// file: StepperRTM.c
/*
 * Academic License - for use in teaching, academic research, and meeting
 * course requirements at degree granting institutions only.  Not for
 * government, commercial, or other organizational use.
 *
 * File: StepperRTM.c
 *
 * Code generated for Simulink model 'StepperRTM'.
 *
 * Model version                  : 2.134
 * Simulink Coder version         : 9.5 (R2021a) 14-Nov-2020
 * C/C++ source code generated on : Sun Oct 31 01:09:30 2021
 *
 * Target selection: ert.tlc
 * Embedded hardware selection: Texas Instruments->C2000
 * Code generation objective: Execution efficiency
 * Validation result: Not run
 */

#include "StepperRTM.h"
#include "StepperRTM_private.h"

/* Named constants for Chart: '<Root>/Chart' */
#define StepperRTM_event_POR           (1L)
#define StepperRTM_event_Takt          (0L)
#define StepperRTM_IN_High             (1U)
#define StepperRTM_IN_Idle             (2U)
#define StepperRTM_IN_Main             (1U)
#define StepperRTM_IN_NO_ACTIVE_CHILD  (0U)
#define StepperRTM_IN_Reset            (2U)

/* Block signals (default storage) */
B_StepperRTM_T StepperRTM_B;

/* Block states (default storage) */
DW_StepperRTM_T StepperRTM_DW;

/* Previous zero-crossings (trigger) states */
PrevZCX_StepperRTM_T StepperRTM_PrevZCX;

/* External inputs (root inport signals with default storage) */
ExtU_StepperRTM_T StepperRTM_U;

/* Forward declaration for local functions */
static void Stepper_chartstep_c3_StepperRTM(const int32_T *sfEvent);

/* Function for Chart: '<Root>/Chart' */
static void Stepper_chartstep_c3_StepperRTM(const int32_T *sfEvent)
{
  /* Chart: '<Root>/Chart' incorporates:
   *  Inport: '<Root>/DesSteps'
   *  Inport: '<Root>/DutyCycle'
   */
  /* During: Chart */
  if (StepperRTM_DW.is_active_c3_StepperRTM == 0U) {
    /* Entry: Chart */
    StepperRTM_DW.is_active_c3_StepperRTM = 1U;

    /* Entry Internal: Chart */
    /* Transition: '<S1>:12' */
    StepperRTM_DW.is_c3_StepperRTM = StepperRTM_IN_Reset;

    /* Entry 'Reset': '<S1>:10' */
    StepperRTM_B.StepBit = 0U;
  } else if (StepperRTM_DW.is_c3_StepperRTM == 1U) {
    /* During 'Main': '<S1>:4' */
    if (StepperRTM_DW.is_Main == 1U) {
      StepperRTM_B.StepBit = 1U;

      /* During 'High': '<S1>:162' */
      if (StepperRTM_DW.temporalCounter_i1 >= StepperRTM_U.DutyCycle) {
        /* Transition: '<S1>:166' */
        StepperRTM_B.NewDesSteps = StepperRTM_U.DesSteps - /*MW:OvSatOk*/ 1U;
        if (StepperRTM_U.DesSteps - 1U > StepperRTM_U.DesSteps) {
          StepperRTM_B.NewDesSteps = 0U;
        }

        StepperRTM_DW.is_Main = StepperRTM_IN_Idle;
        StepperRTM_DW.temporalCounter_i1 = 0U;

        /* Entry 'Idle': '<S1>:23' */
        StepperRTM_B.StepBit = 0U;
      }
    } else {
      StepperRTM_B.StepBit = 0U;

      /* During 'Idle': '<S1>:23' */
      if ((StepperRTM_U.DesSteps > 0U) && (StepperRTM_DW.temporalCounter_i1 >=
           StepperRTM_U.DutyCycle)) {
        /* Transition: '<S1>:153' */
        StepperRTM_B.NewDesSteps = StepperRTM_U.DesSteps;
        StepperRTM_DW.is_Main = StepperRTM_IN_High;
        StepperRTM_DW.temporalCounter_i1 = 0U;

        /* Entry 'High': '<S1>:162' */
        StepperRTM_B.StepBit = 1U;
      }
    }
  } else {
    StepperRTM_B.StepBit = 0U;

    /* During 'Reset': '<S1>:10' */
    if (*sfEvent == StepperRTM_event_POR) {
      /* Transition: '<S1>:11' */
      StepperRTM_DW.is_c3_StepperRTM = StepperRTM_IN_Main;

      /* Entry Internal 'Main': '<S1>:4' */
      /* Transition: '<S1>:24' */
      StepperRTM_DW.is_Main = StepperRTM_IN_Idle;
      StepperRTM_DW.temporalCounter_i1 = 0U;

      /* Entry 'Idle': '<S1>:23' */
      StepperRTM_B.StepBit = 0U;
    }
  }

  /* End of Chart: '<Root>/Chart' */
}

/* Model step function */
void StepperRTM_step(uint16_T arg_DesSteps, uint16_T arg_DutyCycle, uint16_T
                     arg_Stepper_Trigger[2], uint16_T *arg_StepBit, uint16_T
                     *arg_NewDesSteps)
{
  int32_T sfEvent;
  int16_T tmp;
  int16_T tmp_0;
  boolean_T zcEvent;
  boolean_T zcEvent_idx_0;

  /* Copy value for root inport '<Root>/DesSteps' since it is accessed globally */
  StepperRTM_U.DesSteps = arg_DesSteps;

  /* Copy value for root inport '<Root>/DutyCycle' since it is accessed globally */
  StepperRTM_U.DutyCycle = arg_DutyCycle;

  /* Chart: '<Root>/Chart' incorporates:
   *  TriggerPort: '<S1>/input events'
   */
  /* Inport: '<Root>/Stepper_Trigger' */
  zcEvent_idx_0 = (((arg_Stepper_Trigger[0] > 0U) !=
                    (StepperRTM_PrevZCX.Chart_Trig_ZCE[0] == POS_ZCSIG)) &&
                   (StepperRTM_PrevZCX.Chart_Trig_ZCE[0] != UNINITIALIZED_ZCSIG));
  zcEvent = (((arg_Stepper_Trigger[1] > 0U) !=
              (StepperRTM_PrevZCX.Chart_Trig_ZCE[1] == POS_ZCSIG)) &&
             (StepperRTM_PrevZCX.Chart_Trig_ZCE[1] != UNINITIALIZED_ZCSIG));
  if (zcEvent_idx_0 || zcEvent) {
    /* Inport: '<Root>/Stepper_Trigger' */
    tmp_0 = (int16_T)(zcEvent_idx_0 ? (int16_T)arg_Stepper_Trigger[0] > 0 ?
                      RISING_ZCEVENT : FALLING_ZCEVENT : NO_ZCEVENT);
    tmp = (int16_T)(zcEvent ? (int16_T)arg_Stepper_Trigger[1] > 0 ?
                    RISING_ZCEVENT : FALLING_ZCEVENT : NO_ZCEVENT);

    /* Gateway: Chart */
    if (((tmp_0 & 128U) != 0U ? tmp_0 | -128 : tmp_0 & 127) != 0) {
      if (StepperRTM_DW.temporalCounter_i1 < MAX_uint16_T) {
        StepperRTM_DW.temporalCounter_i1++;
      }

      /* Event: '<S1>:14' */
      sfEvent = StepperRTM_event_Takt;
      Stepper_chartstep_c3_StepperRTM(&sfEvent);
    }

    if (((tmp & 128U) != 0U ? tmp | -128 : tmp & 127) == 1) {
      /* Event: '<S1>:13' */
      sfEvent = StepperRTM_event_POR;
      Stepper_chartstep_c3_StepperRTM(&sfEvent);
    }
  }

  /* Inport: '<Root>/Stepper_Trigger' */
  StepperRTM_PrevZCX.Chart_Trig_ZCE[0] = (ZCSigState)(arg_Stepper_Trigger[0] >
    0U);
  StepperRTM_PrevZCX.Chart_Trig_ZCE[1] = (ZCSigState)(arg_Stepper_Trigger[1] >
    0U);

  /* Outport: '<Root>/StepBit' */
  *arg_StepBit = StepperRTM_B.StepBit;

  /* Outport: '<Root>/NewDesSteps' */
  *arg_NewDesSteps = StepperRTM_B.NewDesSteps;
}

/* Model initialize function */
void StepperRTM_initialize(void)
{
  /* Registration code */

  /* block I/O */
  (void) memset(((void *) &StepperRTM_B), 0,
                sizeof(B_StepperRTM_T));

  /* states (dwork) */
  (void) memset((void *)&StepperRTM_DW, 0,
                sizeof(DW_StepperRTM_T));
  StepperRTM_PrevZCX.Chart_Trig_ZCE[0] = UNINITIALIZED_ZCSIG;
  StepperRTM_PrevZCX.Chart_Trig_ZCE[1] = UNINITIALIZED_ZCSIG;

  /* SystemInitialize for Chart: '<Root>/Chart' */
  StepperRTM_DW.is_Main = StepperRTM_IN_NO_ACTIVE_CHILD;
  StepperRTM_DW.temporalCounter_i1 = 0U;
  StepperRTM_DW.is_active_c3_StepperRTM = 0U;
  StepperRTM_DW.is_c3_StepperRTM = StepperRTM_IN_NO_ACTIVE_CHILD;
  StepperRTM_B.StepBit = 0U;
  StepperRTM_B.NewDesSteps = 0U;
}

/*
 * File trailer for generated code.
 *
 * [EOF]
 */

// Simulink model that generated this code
simulink model "StepperRTM"  (R2021a)
settings: Solver=FixedStepDiscrete  StartTime=0.0  StopTime=Inf  FixedStep=TSampleStepper  MaxStep=1e-3  RelTol=1e-3  EnableMultiTasking=on

== system StepperRTM ==
  DesSteps : Inport  OutDataTypeStr=uint16
  DutyCycle : Inport  Port=2  OutDataTypeStr=uint16
  Stepper_Trigger : Inport  Port=3  OutDataTypeStr=uint8
  Chart : Stateflow chart  TreatAsAtomicUnit=on
  StepBit : Outport  OutDataTypeStr=uint16
  NewDesSteps : Outport  Port=2  OutDataTypeStr=uint16
  wires:
  Stepper_Trigger/1 -> Chart/Trigger
  DesSteps/1 -> Chart/1(DesSteps)  "DesSteps"
  Chart/1(StepBit) -> StepBit/1
  Chart/2(NewDesSteps) -> NewDesSteps/1
  DutyCycle/1 -> Chart/2(DutyCycle)  "DutyCycle"

== stateflow chart StepperRTM/Chart ==
  settings: sampleTime=TSample
  state Reset
    en: StepBit = 0;
  state Main
    state Idle
      en: StepBit = 0;
    state High
      en: StepBit = 1;
    (default) -> Idle
    Idle -> High : [DesSteps > 0 && after(DutyCycle, Takt)]{NewDesSteps = DesSteps;}
    High -> Idle : [after(DutyCycle,Takt)]{NewDesSteps = (DesSteps - 1);}
  (default) -> Reset
  Reset -> Main : POR
  data: StepBit output uint16; DesSteps input uint16 =0; NewDesSteps output uint16 =0; DutyCycle input uint16
  events: Takt input EITHER_EDGE_EVENT; POR input RISING_EDGE_EVENT
